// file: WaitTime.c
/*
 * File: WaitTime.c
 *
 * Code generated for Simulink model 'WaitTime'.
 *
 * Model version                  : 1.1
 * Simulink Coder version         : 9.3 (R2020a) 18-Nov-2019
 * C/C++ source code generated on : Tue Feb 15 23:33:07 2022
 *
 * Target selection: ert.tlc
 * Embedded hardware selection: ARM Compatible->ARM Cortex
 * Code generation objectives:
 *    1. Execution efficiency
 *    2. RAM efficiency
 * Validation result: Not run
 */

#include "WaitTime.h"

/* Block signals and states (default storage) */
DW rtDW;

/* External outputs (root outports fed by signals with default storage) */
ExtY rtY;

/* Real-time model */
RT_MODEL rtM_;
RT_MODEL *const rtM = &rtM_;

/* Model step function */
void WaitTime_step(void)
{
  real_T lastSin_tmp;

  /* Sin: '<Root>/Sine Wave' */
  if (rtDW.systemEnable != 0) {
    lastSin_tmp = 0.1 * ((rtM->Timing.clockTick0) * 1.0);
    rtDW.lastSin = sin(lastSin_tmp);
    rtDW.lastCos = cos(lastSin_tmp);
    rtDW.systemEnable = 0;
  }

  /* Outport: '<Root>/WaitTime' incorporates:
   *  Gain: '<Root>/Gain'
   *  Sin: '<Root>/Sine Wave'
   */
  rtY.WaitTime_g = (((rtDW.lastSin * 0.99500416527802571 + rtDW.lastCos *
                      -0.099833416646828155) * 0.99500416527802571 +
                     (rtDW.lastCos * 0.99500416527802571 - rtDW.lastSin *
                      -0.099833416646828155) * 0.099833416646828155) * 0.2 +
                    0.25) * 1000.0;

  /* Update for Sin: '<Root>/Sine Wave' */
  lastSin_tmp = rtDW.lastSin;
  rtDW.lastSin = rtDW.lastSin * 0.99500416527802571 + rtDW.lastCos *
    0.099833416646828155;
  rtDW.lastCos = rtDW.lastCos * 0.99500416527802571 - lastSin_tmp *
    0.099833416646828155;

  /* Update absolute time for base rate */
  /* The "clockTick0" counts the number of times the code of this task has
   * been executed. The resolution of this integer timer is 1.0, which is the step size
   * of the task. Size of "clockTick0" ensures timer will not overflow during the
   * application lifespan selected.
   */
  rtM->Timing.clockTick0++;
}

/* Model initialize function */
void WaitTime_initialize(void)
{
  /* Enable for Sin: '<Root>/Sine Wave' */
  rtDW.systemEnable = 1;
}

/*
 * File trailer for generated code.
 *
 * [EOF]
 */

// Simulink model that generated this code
simulink model "WaitTime"  (R2020a)
settings: Solver=VariableStepAuto  StartTime=0.0  StopTime=500  RelTol=1e-3

== system WaitTime ==
  Gain : Gain  Gain=1000
  Sine Wave : Sin  Amplitude=0.2  Bias=0.25  Frequency=0.1  SampleTime=1
  WaitTime : Outport
  wires:
  Sine Wave/1 -> Gain/1
  Gain/1 -> WaitTime/1
